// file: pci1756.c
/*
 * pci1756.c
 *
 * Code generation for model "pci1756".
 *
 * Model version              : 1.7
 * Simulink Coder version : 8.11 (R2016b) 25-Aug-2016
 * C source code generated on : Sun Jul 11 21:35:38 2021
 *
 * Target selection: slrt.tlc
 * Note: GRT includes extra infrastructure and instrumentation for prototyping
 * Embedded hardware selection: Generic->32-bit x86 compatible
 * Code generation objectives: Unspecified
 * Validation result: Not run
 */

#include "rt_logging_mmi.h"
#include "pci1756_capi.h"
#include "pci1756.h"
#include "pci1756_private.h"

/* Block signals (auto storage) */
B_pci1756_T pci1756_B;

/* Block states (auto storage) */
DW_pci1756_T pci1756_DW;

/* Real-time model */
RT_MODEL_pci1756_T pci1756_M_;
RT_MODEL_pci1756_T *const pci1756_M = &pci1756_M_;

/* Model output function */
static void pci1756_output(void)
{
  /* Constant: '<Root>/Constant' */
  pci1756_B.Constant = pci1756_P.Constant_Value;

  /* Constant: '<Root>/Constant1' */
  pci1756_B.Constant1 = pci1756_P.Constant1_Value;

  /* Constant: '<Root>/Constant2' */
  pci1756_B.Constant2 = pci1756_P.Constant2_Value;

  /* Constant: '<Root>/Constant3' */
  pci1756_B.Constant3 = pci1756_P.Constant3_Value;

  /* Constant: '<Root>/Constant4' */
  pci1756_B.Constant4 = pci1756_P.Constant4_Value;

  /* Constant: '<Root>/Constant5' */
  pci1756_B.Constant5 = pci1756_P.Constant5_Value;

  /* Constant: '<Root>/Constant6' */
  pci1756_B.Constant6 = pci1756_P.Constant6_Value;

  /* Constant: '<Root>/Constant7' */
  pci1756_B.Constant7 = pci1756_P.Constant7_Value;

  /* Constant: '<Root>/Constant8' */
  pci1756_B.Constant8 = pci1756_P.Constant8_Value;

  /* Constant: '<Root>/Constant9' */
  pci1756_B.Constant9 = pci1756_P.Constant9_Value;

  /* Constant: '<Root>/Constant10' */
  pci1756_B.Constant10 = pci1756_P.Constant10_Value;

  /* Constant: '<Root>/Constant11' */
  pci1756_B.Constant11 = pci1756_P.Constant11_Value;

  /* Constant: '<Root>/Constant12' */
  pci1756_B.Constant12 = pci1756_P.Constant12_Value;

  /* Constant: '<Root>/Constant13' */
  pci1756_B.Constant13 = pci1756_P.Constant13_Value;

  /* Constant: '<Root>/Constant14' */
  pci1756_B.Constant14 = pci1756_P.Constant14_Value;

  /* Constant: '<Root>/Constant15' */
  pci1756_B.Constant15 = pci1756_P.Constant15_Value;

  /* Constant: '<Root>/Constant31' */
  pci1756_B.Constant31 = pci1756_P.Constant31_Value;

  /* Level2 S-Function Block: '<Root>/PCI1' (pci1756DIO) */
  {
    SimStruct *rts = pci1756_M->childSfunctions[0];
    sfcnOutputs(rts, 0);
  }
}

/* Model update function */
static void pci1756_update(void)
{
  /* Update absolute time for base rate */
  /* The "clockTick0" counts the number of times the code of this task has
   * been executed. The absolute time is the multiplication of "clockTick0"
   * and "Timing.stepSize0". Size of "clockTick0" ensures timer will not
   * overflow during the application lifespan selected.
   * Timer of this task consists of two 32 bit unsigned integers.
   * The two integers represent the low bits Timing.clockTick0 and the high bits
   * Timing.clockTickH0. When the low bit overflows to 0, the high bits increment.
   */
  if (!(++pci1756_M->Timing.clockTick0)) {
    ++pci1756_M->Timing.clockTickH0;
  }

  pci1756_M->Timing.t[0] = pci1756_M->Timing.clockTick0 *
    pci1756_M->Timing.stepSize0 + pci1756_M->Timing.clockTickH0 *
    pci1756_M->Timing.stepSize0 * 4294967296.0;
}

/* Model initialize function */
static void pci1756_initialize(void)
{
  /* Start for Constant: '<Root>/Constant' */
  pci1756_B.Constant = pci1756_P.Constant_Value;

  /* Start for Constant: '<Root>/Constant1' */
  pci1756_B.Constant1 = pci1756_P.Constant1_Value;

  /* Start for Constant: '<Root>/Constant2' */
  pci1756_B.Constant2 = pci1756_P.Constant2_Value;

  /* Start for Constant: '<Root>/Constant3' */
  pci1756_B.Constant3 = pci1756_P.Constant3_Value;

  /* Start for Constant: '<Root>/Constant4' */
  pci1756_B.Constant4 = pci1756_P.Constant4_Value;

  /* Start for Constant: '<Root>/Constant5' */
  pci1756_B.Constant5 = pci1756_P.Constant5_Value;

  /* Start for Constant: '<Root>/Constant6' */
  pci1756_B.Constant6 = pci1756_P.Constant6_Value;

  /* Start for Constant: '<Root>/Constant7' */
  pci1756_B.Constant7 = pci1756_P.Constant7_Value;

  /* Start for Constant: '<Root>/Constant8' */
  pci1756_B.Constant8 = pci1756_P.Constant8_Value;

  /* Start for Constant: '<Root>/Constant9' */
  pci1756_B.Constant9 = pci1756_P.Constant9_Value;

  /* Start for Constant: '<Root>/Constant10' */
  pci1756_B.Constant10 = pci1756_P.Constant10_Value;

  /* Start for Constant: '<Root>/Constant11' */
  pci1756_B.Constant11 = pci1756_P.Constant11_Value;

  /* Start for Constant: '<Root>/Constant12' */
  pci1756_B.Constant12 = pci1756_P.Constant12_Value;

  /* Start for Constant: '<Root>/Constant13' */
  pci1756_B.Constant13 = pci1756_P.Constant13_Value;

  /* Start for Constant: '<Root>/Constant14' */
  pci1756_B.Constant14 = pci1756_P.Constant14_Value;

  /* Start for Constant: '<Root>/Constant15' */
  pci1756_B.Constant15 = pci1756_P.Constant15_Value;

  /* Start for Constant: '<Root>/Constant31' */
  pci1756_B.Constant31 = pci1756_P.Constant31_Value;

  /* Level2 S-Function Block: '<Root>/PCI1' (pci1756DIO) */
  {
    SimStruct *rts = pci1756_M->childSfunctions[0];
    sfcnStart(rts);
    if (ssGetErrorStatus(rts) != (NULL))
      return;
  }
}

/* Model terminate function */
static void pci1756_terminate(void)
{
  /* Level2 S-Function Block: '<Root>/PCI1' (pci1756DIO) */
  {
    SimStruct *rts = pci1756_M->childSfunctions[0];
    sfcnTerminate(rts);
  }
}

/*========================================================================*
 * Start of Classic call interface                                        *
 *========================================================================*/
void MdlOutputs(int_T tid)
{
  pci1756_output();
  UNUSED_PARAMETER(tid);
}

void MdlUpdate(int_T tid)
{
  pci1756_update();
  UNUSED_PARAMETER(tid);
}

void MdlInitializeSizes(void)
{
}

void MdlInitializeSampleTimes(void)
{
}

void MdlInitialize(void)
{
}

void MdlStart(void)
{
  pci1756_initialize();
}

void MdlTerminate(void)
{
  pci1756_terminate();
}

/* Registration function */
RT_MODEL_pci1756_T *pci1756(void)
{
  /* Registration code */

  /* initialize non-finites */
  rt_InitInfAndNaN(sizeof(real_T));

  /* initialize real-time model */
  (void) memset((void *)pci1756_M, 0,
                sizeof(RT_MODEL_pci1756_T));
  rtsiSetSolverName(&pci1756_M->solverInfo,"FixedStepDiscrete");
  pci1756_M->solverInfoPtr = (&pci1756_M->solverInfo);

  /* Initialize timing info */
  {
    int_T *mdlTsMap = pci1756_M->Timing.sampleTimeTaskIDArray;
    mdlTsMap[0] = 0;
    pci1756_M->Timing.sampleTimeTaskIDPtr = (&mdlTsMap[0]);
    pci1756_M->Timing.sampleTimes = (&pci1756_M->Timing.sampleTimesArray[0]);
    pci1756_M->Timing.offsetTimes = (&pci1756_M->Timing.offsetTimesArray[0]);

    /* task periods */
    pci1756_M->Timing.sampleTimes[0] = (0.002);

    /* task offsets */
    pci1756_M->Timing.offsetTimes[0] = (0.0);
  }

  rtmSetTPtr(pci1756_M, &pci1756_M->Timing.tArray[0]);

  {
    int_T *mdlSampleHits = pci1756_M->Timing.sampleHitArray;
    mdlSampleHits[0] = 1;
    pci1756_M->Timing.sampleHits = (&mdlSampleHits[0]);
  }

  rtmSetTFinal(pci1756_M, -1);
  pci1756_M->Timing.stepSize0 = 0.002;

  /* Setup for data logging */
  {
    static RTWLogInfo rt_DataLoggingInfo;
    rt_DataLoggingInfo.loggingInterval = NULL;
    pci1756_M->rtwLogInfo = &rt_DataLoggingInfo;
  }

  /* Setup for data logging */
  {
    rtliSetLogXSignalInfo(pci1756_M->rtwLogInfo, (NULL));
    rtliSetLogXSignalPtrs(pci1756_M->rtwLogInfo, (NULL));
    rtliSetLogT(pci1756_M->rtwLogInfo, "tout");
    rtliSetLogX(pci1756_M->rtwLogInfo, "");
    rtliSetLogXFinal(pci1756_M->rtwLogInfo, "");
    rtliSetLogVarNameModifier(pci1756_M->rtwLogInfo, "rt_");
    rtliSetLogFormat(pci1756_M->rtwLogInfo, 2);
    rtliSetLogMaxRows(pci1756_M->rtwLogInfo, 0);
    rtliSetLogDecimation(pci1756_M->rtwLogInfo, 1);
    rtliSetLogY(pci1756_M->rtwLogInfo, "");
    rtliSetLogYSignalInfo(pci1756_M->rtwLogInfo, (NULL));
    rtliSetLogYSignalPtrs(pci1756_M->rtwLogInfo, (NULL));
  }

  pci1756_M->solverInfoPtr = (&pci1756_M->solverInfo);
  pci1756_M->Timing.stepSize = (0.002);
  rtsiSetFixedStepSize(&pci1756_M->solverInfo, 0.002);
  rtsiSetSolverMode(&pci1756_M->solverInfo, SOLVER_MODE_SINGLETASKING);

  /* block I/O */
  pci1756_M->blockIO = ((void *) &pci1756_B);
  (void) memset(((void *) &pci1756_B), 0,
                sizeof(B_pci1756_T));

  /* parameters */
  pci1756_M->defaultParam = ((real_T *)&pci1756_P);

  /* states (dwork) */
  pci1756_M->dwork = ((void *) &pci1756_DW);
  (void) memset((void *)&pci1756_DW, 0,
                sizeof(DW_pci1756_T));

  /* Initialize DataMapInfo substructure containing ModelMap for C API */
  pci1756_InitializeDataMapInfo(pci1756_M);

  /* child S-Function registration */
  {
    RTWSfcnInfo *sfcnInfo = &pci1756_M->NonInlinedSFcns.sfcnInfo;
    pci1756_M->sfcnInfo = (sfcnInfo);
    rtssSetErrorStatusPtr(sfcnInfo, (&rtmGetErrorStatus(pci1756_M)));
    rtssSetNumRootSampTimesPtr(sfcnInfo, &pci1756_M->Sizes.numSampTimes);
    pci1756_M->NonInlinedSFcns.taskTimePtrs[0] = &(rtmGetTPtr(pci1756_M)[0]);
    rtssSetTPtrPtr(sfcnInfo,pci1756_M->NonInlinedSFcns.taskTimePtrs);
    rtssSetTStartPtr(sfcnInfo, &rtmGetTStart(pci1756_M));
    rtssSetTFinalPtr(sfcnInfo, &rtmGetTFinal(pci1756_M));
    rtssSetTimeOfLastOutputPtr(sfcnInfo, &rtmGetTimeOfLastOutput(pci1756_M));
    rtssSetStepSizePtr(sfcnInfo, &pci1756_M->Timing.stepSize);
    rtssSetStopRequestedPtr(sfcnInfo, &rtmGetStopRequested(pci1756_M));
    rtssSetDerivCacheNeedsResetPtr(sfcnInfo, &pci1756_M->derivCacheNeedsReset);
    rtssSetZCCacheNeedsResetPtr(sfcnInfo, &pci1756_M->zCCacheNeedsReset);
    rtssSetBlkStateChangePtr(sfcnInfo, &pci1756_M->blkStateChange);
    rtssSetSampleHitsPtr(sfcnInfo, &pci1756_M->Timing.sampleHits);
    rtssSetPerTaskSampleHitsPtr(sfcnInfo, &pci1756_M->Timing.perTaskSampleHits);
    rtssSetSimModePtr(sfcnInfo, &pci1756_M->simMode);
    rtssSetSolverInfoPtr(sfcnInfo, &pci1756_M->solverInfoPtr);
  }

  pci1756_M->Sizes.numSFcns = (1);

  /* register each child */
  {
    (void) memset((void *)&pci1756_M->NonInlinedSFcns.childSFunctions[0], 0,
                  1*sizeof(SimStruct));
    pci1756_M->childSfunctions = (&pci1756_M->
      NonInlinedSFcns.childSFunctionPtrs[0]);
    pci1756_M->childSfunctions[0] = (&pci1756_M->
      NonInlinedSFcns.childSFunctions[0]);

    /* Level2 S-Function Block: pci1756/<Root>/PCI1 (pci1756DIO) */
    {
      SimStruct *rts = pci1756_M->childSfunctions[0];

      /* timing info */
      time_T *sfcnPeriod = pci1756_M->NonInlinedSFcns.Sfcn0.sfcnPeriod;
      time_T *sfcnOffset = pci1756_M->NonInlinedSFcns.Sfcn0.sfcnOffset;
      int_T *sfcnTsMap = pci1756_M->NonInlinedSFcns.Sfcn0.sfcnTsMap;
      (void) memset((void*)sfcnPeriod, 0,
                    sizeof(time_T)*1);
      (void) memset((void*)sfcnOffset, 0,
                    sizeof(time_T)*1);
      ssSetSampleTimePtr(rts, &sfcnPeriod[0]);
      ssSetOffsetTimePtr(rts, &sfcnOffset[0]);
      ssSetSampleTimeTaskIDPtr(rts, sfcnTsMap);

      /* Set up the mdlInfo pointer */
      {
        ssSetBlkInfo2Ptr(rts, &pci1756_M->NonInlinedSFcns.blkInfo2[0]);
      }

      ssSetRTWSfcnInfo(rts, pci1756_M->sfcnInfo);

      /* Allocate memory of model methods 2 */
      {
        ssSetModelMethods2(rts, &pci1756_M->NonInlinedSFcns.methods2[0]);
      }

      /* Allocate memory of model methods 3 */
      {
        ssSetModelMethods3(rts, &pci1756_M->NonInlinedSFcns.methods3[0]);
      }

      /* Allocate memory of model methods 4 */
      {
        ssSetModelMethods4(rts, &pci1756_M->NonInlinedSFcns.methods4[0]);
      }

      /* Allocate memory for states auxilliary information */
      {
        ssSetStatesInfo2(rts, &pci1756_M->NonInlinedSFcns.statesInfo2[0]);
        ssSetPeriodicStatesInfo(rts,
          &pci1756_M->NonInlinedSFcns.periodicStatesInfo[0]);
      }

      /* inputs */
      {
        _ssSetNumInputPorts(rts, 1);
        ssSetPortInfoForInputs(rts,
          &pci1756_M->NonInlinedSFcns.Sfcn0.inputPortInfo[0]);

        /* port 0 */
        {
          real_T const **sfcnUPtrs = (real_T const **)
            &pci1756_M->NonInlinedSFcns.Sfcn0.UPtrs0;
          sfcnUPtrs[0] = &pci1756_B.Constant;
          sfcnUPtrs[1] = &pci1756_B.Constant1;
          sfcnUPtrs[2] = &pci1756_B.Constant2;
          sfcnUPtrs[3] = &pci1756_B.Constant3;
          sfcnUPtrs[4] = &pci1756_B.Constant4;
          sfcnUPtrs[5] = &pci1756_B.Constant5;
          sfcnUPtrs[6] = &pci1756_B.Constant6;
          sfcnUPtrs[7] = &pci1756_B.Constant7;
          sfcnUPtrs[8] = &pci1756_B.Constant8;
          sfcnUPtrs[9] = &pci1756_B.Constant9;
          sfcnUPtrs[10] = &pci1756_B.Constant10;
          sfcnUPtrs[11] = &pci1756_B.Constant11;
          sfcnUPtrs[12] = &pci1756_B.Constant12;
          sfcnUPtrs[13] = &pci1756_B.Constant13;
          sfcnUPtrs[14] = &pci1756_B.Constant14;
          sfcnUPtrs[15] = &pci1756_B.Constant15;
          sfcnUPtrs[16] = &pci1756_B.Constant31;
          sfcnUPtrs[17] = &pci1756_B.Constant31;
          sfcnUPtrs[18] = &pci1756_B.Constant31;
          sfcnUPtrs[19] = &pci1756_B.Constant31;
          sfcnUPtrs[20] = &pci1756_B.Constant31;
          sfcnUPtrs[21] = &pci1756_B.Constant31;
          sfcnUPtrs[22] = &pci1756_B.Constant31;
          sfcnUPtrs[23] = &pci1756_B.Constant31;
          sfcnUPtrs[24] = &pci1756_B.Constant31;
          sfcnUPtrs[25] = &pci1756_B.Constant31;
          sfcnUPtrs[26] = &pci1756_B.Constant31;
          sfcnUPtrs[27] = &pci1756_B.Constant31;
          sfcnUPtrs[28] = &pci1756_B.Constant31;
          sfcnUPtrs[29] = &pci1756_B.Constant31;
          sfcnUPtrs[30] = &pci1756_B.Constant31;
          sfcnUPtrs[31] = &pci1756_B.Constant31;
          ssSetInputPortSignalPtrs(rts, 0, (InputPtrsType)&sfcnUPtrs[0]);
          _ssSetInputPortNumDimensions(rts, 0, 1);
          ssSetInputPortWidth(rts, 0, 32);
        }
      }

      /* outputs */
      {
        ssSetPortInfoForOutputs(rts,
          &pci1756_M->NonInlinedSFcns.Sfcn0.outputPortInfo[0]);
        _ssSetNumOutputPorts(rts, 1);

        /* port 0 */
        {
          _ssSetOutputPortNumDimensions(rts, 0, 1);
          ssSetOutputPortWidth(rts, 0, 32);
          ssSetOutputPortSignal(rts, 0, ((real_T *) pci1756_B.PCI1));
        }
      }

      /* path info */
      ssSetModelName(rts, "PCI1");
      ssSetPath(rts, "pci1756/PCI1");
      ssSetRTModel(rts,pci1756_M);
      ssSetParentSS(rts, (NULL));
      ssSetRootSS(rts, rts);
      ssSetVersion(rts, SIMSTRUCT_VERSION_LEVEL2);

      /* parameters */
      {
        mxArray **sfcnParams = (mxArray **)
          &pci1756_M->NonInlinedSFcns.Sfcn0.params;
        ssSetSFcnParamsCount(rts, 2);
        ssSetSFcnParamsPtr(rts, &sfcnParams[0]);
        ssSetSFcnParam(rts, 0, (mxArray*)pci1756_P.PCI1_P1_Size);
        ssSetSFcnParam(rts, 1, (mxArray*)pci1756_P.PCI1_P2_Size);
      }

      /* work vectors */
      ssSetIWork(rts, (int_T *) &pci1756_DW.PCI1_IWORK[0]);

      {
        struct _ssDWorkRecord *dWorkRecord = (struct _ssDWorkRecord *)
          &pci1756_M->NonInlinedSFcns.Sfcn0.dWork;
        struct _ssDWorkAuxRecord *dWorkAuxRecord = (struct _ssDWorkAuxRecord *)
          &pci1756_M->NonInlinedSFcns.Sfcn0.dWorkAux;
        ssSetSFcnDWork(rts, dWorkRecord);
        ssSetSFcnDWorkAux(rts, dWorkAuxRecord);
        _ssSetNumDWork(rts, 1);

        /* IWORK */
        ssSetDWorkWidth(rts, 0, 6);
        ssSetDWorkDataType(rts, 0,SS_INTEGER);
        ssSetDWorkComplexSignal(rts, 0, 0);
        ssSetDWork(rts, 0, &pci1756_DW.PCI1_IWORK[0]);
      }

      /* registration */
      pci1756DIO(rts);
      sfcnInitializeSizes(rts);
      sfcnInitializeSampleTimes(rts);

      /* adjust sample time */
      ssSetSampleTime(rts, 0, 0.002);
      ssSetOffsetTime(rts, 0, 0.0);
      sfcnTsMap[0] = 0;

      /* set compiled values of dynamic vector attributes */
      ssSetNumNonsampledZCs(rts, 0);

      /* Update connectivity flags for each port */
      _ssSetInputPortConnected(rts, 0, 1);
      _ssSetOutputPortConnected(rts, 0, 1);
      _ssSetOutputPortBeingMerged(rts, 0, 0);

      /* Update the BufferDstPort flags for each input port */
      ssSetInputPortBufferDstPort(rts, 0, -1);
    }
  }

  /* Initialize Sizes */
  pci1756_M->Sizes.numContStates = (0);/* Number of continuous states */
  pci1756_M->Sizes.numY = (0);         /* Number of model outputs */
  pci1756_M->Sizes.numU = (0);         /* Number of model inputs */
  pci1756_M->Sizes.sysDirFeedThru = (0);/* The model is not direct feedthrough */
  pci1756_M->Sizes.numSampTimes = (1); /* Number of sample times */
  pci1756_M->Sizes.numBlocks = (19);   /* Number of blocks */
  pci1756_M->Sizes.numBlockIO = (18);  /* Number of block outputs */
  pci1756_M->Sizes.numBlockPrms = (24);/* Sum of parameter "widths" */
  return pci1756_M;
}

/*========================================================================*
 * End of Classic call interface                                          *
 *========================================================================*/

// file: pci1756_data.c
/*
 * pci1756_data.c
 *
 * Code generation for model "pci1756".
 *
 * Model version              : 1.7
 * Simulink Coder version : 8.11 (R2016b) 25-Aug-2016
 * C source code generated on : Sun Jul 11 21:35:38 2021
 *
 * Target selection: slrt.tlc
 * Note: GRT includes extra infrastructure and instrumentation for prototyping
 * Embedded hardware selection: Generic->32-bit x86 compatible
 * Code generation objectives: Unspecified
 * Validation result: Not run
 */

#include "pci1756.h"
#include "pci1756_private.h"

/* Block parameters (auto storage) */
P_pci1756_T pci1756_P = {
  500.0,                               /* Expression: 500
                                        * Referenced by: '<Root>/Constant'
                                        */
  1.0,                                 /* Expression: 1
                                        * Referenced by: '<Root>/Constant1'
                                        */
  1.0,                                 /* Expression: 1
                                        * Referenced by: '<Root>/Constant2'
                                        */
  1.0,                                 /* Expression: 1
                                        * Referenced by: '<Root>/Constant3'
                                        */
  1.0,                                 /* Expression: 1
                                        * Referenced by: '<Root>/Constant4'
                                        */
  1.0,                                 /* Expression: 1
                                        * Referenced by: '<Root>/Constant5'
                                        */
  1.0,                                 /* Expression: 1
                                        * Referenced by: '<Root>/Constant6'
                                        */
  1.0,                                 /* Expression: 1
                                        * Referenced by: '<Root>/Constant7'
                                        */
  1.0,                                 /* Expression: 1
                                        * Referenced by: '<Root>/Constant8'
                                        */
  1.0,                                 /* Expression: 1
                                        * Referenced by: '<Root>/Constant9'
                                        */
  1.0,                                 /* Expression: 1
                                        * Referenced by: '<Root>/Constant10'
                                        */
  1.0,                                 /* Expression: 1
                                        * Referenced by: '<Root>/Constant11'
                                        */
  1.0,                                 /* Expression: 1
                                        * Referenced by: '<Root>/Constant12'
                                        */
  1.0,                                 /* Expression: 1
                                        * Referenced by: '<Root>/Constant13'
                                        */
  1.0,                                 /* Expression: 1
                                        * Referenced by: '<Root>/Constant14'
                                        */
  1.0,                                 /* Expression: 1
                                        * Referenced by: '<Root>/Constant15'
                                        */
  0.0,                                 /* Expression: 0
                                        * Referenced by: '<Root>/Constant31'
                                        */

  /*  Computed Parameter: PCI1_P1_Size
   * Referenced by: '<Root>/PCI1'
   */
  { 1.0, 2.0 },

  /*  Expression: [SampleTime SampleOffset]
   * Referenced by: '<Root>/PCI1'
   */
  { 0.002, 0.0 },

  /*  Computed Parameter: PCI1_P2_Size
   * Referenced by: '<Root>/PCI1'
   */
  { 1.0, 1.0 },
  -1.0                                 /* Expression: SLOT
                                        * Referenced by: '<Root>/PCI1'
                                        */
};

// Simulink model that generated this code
simulink model "pci1756"  (R2016b)
settings: Solver=ode4  StartTime=0.0  StopTime=inf  FixedStep=0.002  RelTol=1e-3  EnableMultiTasking=on

== system pci1756 ==
  note: 输出
  Constant : Constant  Value=500
  Constant{1..15} (15 alike) : Constant
  Constant31 : Constant  Value=0
  Mux : Mux  Inputs=32
  PCI1 : S-Function  FunctionName=pci1756DIO  Parameters=[SampleTime SampleOffset], SLOT  SFunctionDeploymentMode=off  EnableBusSupport=off  mask(PCI1756){Sample=0.002, SLOT=-1}
      mask prompts: Sample "Sample time:"
      mask help:
      | PCI-1756
      | Advantech
      | Digital Input&Output
      mask init:
      | SampleTime =0.002; SampleOffset=0;
  输入 : Display
  wires:
  Constant/1 -> Mux/1
  Constant1/1 -> Mux/2
  Constant2/1 -> Mux/3
  Constant3/1 -> Mux/4
  Constant4/1 -> Mux/5
  Constant5/1 -> Mux/6
  Constant6/1 -> Mux/7
  Constant7/1 -> Mux/8
  Constant8/1 -> Mux/9
  Constant9/1 -> Mux/10
  Constant10/1 -> Mux/11
  Constant11/1 -> Mux/12
  Constant12/1 -> Mux/13
  Constant13/1 -> Mux/14
  Constant14/1 -> Mux/15
  Constant15/1 -> Mux/16
  Mux/1 -> PCI1/1
  PCI1/1 -> 输入/1
  Constant31/1 -> Mux/32, Mux/31, Mux/30, Mux/29, Mux/28, Mux/27, Mux/26, Mux/25, Mux/24, Mux/23, Mux/22, Mux/21, Mux/20, Mux/19, Mux/17, Mux/18
